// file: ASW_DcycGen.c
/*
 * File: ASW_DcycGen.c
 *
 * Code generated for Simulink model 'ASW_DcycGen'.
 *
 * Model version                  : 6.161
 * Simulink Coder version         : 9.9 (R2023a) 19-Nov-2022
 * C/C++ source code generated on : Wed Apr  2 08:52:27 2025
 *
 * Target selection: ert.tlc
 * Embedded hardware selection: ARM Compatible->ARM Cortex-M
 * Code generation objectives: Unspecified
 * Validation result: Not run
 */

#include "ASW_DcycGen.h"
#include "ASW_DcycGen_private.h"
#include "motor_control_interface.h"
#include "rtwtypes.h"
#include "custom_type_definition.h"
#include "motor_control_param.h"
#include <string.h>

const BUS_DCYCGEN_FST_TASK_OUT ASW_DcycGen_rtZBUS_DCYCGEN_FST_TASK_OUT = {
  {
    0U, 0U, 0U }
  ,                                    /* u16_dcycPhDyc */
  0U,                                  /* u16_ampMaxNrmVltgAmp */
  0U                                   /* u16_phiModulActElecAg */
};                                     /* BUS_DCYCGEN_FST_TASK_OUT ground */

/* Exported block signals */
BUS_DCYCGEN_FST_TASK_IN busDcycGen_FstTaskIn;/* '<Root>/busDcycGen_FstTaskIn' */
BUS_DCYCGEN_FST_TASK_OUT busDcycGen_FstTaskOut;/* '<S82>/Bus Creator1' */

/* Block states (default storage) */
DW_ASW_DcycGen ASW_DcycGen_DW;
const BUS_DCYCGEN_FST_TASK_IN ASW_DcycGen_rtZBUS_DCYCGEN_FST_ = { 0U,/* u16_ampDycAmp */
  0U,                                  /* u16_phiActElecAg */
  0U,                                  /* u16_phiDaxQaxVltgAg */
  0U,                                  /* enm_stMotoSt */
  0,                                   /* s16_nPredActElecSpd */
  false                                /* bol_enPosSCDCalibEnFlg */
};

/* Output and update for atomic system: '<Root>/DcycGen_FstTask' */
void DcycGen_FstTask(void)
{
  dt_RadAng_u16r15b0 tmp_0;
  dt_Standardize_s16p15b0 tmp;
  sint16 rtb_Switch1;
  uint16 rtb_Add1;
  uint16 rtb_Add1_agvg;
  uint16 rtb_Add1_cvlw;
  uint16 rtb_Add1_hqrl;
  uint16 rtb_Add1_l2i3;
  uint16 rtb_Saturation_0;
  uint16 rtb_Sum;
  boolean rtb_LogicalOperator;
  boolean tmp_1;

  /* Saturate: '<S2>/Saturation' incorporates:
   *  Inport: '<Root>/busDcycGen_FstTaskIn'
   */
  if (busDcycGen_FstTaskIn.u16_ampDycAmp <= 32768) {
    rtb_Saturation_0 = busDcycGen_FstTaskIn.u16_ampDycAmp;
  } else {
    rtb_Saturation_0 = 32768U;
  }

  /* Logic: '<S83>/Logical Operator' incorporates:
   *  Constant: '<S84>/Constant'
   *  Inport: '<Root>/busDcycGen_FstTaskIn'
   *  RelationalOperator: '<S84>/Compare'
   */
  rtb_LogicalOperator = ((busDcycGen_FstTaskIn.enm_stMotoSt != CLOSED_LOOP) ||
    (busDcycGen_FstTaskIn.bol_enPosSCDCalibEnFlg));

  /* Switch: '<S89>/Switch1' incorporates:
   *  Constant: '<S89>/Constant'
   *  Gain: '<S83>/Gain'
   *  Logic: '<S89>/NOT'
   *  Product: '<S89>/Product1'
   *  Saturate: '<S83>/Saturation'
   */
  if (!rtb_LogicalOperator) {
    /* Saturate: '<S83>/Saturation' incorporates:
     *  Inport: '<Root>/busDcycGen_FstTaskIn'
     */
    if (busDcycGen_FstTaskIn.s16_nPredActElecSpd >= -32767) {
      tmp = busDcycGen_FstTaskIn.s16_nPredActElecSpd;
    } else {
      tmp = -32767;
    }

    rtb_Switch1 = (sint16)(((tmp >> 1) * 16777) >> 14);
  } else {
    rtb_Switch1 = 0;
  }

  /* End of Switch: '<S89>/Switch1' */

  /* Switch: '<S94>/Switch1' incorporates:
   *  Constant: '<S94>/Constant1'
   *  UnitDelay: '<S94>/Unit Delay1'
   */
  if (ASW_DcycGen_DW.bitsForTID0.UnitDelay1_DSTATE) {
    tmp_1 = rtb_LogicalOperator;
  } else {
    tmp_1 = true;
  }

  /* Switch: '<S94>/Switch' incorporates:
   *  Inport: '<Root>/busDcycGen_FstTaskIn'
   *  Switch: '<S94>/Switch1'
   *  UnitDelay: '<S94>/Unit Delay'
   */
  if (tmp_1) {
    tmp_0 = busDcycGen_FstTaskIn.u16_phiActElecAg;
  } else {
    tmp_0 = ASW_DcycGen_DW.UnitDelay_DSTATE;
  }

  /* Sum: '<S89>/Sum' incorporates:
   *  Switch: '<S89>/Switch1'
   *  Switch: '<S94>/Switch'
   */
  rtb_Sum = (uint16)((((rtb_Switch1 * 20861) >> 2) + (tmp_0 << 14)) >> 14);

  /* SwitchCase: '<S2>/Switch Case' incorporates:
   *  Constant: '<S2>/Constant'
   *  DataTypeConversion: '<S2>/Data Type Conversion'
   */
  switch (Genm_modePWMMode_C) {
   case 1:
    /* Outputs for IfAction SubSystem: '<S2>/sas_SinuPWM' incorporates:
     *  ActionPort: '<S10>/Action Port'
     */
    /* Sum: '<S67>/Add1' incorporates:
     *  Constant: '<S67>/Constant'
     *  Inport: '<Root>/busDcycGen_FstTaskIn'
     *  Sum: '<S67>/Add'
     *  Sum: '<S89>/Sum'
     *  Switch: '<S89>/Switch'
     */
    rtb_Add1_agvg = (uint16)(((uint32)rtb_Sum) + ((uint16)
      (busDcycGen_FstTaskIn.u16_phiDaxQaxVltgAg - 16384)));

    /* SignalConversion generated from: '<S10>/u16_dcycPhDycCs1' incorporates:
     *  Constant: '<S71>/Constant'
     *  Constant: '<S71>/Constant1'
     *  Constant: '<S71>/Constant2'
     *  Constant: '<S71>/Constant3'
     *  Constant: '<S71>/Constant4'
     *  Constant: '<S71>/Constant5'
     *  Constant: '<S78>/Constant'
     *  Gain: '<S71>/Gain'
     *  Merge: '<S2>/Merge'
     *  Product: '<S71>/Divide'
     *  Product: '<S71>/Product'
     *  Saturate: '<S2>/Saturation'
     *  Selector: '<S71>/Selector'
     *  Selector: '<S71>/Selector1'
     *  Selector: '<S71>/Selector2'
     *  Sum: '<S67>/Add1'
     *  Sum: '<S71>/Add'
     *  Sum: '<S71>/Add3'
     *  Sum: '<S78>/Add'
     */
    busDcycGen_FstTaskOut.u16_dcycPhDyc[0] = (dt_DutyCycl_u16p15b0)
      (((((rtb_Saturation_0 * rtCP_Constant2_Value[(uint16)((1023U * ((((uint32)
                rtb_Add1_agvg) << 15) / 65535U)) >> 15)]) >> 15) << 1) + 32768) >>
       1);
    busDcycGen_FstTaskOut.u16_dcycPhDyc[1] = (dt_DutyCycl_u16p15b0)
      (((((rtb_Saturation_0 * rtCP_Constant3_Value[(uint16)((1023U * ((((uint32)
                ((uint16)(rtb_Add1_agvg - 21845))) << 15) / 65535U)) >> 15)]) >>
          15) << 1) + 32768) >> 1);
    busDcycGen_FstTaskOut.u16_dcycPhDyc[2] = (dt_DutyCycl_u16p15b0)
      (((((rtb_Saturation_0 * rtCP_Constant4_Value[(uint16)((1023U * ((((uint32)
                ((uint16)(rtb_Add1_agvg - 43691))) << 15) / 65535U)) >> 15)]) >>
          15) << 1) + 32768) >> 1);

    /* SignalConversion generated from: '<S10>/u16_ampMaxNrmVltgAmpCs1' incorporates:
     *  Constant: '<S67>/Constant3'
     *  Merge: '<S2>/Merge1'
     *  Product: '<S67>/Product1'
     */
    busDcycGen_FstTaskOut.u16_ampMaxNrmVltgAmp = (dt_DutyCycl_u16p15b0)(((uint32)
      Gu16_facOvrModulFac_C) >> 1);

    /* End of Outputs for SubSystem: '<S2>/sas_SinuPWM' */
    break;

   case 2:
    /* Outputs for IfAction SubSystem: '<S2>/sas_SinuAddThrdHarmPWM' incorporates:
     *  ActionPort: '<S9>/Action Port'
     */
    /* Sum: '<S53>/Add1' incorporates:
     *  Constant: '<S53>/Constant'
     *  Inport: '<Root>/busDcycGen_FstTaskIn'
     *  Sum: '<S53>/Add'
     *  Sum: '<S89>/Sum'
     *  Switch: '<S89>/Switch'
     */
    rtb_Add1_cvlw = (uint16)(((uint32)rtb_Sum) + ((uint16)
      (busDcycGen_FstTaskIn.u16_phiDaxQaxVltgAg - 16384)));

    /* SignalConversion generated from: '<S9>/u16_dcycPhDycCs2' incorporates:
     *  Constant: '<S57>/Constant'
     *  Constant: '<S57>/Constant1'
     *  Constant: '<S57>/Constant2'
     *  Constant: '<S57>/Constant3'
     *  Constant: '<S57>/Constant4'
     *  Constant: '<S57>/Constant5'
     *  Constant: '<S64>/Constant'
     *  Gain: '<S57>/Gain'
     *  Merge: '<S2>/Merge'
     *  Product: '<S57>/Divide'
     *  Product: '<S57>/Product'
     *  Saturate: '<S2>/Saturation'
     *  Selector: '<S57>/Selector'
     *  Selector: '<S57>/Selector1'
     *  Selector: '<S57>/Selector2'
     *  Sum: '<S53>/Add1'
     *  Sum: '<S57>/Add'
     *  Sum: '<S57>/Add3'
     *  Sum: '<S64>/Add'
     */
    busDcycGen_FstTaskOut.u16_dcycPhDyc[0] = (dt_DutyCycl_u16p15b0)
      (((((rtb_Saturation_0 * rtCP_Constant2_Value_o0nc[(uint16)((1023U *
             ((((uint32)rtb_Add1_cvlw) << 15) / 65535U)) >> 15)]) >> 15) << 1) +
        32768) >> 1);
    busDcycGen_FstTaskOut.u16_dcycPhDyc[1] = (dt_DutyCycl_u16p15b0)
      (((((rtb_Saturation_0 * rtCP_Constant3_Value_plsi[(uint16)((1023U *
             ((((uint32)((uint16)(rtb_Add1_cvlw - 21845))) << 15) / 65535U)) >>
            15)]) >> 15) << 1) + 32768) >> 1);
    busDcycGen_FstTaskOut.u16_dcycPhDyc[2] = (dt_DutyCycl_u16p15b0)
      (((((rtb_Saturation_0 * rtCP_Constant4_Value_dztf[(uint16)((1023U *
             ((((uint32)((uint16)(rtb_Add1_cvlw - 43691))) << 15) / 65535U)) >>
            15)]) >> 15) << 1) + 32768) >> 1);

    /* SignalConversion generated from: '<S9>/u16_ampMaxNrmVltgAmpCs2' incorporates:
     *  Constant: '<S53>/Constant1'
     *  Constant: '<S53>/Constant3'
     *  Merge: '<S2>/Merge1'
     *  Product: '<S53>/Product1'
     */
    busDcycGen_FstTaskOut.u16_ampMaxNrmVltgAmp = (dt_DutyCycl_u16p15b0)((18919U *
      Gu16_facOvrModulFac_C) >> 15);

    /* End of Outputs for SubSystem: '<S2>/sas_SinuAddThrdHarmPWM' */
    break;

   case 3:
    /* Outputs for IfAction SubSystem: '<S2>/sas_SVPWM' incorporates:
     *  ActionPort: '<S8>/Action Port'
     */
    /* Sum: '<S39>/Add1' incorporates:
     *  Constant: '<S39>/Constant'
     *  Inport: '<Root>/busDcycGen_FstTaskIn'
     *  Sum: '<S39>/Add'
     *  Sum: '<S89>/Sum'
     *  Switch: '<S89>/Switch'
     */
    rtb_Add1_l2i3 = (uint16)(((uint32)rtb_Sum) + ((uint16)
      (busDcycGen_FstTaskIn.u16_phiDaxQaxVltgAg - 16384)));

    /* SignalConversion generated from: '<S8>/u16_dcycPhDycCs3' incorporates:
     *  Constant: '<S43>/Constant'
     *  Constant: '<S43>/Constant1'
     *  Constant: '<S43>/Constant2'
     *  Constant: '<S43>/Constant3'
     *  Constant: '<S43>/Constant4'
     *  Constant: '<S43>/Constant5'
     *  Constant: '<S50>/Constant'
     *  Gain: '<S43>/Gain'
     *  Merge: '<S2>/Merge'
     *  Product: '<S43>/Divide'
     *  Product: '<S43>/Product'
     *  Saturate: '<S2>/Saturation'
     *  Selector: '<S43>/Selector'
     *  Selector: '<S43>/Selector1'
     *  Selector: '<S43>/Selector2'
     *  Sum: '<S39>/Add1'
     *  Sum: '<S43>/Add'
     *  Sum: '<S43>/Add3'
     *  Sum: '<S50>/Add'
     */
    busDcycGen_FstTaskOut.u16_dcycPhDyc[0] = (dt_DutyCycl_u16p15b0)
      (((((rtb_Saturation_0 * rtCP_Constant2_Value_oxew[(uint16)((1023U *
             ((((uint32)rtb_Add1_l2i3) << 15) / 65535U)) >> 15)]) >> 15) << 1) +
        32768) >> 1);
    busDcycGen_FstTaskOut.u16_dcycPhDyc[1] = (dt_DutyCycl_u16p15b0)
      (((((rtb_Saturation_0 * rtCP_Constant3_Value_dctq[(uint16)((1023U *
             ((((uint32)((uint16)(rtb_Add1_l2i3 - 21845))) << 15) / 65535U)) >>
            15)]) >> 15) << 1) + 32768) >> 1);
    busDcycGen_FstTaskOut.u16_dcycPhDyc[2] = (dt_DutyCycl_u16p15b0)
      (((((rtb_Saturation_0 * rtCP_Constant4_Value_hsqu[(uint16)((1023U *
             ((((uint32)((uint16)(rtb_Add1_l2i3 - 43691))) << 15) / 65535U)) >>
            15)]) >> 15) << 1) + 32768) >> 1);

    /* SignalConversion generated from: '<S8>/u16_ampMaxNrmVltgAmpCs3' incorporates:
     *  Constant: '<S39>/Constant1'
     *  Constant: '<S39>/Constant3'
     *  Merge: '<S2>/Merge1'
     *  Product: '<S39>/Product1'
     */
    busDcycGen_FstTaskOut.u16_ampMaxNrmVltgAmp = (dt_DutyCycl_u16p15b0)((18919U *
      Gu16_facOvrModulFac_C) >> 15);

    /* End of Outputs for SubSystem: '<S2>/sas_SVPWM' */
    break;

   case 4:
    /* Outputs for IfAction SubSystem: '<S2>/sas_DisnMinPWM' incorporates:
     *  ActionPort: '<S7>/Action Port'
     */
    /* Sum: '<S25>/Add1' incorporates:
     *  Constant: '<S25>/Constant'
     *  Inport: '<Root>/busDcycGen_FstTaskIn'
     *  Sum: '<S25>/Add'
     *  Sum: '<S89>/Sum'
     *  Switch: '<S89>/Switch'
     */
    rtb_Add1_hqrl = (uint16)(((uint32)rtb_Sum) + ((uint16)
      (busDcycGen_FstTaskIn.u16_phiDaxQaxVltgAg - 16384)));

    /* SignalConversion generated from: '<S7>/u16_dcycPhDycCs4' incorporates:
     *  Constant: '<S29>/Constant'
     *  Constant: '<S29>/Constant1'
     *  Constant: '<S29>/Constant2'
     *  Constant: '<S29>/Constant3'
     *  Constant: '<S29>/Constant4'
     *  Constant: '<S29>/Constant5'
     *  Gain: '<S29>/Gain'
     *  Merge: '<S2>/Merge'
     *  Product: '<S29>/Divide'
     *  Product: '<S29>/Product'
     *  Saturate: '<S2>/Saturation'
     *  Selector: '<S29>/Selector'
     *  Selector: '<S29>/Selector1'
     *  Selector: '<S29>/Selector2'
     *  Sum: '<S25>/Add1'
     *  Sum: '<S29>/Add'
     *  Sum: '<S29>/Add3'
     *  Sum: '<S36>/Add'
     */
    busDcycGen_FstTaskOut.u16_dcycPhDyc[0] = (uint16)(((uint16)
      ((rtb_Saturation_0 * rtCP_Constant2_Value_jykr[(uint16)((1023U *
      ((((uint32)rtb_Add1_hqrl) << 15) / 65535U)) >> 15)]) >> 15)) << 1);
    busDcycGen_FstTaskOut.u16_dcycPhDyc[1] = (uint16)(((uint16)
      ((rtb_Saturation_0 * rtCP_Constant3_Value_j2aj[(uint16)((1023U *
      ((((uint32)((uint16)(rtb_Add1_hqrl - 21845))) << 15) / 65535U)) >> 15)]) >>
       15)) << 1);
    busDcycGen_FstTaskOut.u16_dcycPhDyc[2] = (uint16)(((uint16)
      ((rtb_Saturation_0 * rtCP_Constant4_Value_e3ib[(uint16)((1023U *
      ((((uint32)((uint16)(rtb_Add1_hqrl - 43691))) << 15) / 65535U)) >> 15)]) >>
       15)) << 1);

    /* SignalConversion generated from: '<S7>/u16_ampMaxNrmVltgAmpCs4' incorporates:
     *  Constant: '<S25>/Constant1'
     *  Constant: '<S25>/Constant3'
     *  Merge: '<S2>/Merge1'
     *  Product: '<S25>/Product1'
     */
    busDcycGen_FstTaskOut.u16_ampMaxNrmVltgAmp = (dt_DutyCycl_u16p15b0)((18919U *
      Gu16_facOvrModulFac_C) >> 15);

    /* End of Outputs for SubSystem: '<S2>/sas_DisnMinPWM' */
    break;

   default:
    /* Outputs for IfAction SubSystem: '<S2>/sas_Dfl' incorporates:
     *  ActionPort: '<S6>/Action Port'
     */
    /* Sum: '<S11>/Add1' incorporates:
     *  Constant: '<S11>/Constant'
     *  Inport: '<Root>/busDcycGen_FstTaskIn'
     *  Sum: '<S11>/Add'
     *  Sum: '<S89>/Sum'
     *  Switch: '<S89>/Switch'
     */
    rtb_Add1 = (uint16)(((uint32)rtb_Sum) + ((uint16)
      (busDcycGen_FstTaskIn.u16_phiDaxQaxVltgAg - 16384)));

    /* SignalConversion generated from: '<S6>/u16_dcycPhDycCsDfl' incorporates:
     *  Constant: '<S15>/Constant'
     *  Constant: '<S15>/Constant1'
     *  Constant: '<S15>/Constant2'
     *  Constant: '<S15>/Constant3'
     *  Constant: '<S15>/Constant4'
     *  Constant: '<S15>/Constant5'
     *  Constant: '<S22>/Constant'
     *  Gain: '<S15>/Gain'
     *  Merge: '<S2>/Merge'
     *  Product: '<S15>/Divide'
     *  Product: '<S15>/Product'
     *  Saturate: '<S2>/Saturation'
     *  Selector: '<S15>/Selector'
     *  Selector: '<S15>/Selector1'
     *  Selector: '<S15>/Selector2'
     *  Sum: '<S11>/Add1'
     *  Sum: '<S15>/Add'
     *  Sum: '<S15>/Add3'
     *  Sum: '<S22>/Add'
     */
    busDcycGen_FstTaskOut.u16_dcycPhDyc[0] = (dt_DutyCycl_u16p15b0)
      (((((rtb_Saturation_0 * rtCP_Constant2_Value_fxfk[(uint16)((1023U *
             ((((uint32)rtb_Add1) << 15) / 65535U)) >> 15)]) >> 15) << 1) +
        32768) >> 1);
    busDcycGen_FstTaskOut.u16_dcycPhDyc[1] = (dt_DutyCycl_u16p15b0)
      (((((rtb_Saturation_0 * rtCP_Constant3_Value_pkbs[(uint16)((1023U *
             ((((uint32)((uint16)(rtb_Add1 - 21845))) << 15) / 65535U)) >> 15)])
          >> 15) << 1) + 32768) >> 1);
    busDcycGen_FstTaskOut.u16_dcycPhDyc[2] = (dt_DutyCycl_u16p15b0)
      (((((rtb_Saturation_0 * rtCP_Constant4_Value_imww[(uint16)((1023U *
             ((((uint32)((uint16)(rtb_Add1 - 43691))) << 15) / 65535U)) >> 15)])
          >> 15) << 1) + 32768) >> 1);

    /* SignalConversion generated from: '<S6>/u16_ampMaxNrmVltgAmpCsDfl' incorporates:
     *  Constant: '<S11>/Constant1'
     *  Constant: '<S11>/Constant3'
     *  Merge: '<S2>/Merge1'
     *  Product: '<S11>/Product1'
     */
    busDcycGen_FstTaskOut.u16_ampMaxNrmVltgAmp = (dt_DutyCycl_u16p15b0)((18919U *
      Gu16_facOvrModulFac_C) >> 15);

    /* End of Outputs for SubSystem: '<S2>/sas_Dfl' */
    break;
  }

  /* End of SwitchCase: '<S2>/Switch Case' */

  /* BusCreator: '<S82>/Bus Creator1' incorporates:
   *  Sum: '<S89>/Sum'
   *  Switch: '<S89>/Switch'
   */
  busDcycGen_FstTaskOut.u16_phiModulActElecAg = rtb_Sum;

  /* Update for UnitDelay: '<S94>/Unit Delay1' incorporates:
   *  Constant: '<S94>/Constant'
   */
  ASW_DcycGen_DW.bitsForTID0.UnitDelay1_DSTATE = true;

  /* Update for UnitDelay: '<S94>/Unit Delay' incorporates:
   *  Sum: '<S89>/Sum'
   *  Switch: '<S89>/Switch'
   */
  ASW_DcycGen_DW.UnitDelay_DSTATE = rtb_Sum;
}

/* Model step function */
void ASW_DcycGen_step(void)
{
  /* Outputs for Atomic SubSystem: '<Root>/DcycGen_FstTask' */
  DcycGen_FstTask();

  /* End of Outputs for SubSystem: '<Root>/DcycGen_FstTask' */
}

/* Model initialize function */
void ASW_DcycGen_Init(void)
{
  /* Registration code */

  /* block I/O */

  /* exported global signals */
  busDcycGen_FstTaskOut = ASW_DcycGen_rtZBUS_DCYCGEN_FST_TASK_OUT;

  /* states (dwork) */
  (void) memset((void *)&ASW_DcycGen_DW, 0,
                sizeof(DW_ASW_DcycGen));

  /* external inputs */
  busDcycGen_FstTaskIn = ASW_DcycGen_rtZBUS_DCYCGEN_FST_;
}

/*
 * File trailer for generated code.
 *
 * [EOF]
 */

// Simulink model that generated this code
simulink model "ASW_DcycGen"  (R2023a)
settings: configuration reference "cfg_FastTaskCodeGeneration_v01" (kept outside this file)
undefined symbols (not defined in the file): Cdbl_tiFstTaskSmpTi

== system ASW_DcycGen ==
  busDcycGen_FstTaskIn : Inport  OutDataTypeStr=Bus: BUS_DCYCGEN_FST_TASK_IN  SampleTime=round(double(Cdbl_tiFstTaskSmpTi),8)  BusOutputAsStruct=on
  DcycGen_FstTask : Subsystem  TreatAsAtomicUnit=on  RTWFcnName=DcycGen_FstTask
  busDcycGen_FstTaskOut : Outport  OutDataTypeStr=Bus: BUS_DCYCGEN_FST_TASK_OUT  SampleTime=round(double(Cdbl_tiFstTaskSmpTi),8)
  wires:
  busDcycGen_FstTaskIn/1 -> DcycGen_FstTask/1(busDcycGen_FstTaskIn)
  DcycGen_FstTask/1(busDcycGen_FstTaskOut) -> busDcycGen_FstTaskOut/1

== system ASW_DcycGen/DcycGen_FstTask ==
  busDcycGen_FstTaskIn : Inport
  rss_DycCalc : Subsystem  ReferencedSubsystem=rss_DycCalc
  vrs_FstTaskIn : Subsystem  Variant=on  VariantControlMode=label  VariantControl=Choice  LabelModeActiveChoice=cstSensCtrlLbl
  vrs_FstTaskOut : Subsystem  Variant=on  VariantControlMode=label  VariantControl=Choice  LabelModeActiveChoice=cstSensCtrlLbl
  vrs_ModulElecAgCalc : Subsystem  Variant=on  VariantControlMode=label  VariantControl=Choice  LabelModeActiveChoice=cstSensCtrlLbl
  busDcycGen_FstTaskOut : Outport
  wires:
  [u16_phiModulActElecAg] -> vrs_FstTaskOut/3(u16_phiModulActElecAg)
  [u16_ampMaxNrmVltgAmp] -> vrs_FstTaskOut/2(u16_ampMaxNrmVltgAmp)
  vrs_FstTaskIn/4(enm_stMotoSt) -> [enm_stMotoSt]
  vrs_FstTaskIn/1(u16_ampDycAmp) -> [u16_ampDycAmp]
  vrs_FstTaskOut/1(busDcycGen_FstTaskOut) -> busDcycGen_FstTaskOut/1  "busDcycGen_FstTaskOut"
  [u16_phiDaxQaxVltgAg] -> rss_DycCalc/3
  vrs_FstTaskIn/5(s16_nPredActElecSpd) -> [s16_nPredActElecSpd]
  rss_DycCalc/1 -> [u16_dcycPhDyc]
  vrs_FstTaskIn/2(u16_phiActElecAg) -> [u16_phiActElecAg]
  busDcycGen_FstTaskIn/1 -> vrs_FstTaskIn/1(busDcycGen_FstTaskIn)  "busDcycGen_FstTaskIn"
  [u16_dcycPhDyc] -> vrs_FstTaskOut/1(u16_dcycPhDyc)
  [u16_ampDycAmp] -> rss_DycCalc/1
  rss_DycCalc/2 -> [u16_ampMaxNrmVltgAmp]
  [u16_phiModulActElecAg] -> rss_DycCalc/2
  vrs_FstTaskIn/3(u16_phiDaxQaxVltgAg) -> [u16_phiDaxQaxVltgAg]
  vrs_FstTaskIn/6(bol_enPosSCDCalibEnFlg) -> [bol_enPosSCDCalibEnFlg]
  [u16_phiActElecAg] -> vrs_ModulElecAgCalc/1(u16_phiActElecAg)
  [s16_nPredActElecSpd] -> vrs_ModulElecAgCalc/2(s16_nPredActElecSpd)
  [enm_stMotoSt] -> vrs_ModulElecAgCalc/3(enm_stMotoSt)
  [bol_enPosSCDCalibEnFlg] -> vrs_ModulElecAgCalc/4(bol_enPosSCDCalibEnFlg)
  vrs_ModulElecAgCalc/1(u16_phiModulActElecAg) -> [u16_phiModulActElecAg]

== system ASW_DcycGen/DcycGen_FstTask/vrs_FstTaskIn ==
  busDcycGen_FstTaskIn : Inport
  sss_FstTaskInSenl : Subsystem  VariantControl=cstSenlCtrlLbl
  sss_FstTaskInSens : Subsystem  VariantControl=cstSensCtrlLbl
  u16_ampDycAmp : Outport
  u16_phiActElecAg : Outport  Port=2
  u16_phiDaxQaxVltgAg : Outport  Port=3
  enm_stMotoSt : Outport  Port=4
  s16_nPredActElecSpd : Outport  Port=5
  bol_enPosSCDCalibEnFlg : Outport  Port=6

== system ASW_DcycGen/DcycGen_FstTask/vrs_FstTaskOut ==
  u16_dcycPhDyc : Inport
  u16_ampMaxNrmVltgAmp : Inport  Port=2
  u16_phiModulActElecAg : Inport  Port=3
  sss_FstTaskOutSenl : Subsystem  VariantControl=cstSenlCtrlLbl
  sss_FstTaskOutSens : Subsystem  VariantControl=cstSensCtrlLbl
  busDcycGen_FstTaskOut : Outport

== system ASW_DcycGen/DcycGen_FstTask/vrs_ModulElecAgCalc ==
  u16_phiActElecAg : Inport
  s16_nPredActElecSpd : Inport  Port=2
  enm_stMotoSt : Inport  Port=3
  bol_enPosSCDCalibEnFlg : Inport  Port=4
  rss_ModulElecAgCalcSenl : Subsystem  VariantControl=cstSenlCtrlLbl  ReferencedSubsystem=rss_ModulElecAgCalcSenl
  rss_ModulElecAgCalcSens : Subsystem  VariantControl=cstSensCtrlLbl  ReferencedSubsystem=rss_ModulElecAgCalcSens
  u16_phiModulActElecAg : Outport

== system ASW_DcycGen/DcycGen_FstTask/vrs_FstTaskIn/sss_FstTaskInSenl ==
  BusElementIn : Inport  PortName=busDcycGen_FstTaskIn  Element=u16_ampDycAmp
  BusElementIn1 : Inport  PortName=busDcycGen_FstTaskIn  Element=u16_phiActElecAg
  BusElementIn2 : Inport  PortName=busDcycGen_FstTaskIn  Element=u16_phiDaxQaxVltgAg
  BusElementIn3 : Inport  PortName=busDcycGen_FstTaskIn  Element=enm_stMotoSt
  BusElementIn4 : Inport  PortName=busDcycGen_FstTaskIn  Element=s16_nPredActElecSpd
  u16_ampDycAmp : Outport
  u16_phiActElecAg : Outport  Port=2
  u16_phiDaxQaxVltgAg : Outport  Port=3
  enm_stMotoSt : Outport  Port=4
  s16_nPredActElecSpd : Outport  Port=5
  wires:
  BusElementIn/1 -> u16_ampDycAmp/1
  BusElementIn1/1 -> u16_phiActElecAg/1
  BusElementIn2/1 -> u16_phiDaxQaxVltgAg/1
  BusElementIn3/1 -> enm_stMotoSt/1
  BusElementIn4/1 -> s16_nPredActElecSpd/1

== system ASW_DcycGen/DcycGen_FstTask/vrs_FstTaskIn/sss_FstTaskInSens ==
  BusElementIn3 : Inport  PortName=busDcycGen_FstTaskIn  Element=u16_ampDycAmp
  BusElementIn4 : Inport  PortName=busDcycGen_FstTaskIn  Element=u16_phiActElecAg
  BusElementIn5 : Inport  PortName=busDcycGen_FstTaskIn  Element=u16_phiDaxQaxVltgAg
  BusElementIn6 : Inport  PortName=busDcycGen_FstTaskIn  Element=enm_stMotoSt
  BusElementIn7 : Inport  PortName=busDcycGen_FstTaskIn  Element=s16_nPredActElecSpd
  BusElementIn8 : Inport  PortName=busDcycGen_FstTaskIn  Element=bol_enPosSCDCalibEnFlg
  u16_ampDycAmp : Outport
  u16_phiActElecAg : Outport  Port=2
  u16_phiDaxQaxVltgAg : Outport  Port=3
  enm_stMotoSt : Outport  Port=4
  s16_nPredActElecSpd : Outport  Port=5
  bol_enPosSCDCalibEnFlg : Outport  Port=6
  wires:
  BusElementIn3/1 -> u16_ampDycAmp/1
  BusElementIn4/1 -> u16_phiActElecAg/1
  BusElementIn5/1 -> u16_phiDaxQaxVltgAg/1
  BusElementIn6/1 -> enm_stMotoSt/1
  BusElementIn7/1 -> s16_nPredActElecSpd/1
  BusElementIn8/1 -> bol_enPosSCDCalibEnFlg/1

== system ASW_DcycGen/DcycGen_FstTask/vrs_FstTaskOut/sss_FstTaskOutSenl ==
  u16_dcycPhDyc : Inport
  u16_ampMaxNrmVltgAmp : Inport  Port=2
  u16_phiModulActElecAg : Inport  Port=3
  Bus Creator1 : BusCreator  Inputs=3  OutDataTypeStr=Bus: BUS_DCYCGEN_FST_TASK_OUT  NonVirtualBus=on
  busDcycGen_FstTaskOut : Outport
  wires:
  u16_dcycPhDyc/1 -> Bus Creator1/1
  u16_ampMaxNrmVltgAmp/1 -> Bus Creator1/2
  u16_phiModulActElecAg/1 -> Bus Creator1/3
  Bus Creator1/1 -> busDcycGen_FstTaskOut/1

== system ASW_DcycGen/DcycGen_FstTask/vrs_FstTaskOut/sss_FstTaskOutSens ==
  u16_dcycPhDyc : Inport
  u16_ampMaxNrmVltgAmp : Inport  Port=2
  u16_phiModulActElecAg : Inport  Port=3
  Bus Creator1 : BusCreator  Inputs=3  OutDataTypeStr=Bus: BUS_DCYCGEN_FST_TASK_OUT  NonVirtualBus=on
  busDcycGen_FstTaskOut : Outport
  wires:
  u16_dcycPhDyc/1 -> Bus Creator1/1
  u16_ampMaxNrmVltgAmp/1 -> Bus Creator1/2
  u16_phiModulActElecAg/1 -> Bus Creator1/3
  Bus Creator1/1 -> busDcycGen_FstTaskOut/1
